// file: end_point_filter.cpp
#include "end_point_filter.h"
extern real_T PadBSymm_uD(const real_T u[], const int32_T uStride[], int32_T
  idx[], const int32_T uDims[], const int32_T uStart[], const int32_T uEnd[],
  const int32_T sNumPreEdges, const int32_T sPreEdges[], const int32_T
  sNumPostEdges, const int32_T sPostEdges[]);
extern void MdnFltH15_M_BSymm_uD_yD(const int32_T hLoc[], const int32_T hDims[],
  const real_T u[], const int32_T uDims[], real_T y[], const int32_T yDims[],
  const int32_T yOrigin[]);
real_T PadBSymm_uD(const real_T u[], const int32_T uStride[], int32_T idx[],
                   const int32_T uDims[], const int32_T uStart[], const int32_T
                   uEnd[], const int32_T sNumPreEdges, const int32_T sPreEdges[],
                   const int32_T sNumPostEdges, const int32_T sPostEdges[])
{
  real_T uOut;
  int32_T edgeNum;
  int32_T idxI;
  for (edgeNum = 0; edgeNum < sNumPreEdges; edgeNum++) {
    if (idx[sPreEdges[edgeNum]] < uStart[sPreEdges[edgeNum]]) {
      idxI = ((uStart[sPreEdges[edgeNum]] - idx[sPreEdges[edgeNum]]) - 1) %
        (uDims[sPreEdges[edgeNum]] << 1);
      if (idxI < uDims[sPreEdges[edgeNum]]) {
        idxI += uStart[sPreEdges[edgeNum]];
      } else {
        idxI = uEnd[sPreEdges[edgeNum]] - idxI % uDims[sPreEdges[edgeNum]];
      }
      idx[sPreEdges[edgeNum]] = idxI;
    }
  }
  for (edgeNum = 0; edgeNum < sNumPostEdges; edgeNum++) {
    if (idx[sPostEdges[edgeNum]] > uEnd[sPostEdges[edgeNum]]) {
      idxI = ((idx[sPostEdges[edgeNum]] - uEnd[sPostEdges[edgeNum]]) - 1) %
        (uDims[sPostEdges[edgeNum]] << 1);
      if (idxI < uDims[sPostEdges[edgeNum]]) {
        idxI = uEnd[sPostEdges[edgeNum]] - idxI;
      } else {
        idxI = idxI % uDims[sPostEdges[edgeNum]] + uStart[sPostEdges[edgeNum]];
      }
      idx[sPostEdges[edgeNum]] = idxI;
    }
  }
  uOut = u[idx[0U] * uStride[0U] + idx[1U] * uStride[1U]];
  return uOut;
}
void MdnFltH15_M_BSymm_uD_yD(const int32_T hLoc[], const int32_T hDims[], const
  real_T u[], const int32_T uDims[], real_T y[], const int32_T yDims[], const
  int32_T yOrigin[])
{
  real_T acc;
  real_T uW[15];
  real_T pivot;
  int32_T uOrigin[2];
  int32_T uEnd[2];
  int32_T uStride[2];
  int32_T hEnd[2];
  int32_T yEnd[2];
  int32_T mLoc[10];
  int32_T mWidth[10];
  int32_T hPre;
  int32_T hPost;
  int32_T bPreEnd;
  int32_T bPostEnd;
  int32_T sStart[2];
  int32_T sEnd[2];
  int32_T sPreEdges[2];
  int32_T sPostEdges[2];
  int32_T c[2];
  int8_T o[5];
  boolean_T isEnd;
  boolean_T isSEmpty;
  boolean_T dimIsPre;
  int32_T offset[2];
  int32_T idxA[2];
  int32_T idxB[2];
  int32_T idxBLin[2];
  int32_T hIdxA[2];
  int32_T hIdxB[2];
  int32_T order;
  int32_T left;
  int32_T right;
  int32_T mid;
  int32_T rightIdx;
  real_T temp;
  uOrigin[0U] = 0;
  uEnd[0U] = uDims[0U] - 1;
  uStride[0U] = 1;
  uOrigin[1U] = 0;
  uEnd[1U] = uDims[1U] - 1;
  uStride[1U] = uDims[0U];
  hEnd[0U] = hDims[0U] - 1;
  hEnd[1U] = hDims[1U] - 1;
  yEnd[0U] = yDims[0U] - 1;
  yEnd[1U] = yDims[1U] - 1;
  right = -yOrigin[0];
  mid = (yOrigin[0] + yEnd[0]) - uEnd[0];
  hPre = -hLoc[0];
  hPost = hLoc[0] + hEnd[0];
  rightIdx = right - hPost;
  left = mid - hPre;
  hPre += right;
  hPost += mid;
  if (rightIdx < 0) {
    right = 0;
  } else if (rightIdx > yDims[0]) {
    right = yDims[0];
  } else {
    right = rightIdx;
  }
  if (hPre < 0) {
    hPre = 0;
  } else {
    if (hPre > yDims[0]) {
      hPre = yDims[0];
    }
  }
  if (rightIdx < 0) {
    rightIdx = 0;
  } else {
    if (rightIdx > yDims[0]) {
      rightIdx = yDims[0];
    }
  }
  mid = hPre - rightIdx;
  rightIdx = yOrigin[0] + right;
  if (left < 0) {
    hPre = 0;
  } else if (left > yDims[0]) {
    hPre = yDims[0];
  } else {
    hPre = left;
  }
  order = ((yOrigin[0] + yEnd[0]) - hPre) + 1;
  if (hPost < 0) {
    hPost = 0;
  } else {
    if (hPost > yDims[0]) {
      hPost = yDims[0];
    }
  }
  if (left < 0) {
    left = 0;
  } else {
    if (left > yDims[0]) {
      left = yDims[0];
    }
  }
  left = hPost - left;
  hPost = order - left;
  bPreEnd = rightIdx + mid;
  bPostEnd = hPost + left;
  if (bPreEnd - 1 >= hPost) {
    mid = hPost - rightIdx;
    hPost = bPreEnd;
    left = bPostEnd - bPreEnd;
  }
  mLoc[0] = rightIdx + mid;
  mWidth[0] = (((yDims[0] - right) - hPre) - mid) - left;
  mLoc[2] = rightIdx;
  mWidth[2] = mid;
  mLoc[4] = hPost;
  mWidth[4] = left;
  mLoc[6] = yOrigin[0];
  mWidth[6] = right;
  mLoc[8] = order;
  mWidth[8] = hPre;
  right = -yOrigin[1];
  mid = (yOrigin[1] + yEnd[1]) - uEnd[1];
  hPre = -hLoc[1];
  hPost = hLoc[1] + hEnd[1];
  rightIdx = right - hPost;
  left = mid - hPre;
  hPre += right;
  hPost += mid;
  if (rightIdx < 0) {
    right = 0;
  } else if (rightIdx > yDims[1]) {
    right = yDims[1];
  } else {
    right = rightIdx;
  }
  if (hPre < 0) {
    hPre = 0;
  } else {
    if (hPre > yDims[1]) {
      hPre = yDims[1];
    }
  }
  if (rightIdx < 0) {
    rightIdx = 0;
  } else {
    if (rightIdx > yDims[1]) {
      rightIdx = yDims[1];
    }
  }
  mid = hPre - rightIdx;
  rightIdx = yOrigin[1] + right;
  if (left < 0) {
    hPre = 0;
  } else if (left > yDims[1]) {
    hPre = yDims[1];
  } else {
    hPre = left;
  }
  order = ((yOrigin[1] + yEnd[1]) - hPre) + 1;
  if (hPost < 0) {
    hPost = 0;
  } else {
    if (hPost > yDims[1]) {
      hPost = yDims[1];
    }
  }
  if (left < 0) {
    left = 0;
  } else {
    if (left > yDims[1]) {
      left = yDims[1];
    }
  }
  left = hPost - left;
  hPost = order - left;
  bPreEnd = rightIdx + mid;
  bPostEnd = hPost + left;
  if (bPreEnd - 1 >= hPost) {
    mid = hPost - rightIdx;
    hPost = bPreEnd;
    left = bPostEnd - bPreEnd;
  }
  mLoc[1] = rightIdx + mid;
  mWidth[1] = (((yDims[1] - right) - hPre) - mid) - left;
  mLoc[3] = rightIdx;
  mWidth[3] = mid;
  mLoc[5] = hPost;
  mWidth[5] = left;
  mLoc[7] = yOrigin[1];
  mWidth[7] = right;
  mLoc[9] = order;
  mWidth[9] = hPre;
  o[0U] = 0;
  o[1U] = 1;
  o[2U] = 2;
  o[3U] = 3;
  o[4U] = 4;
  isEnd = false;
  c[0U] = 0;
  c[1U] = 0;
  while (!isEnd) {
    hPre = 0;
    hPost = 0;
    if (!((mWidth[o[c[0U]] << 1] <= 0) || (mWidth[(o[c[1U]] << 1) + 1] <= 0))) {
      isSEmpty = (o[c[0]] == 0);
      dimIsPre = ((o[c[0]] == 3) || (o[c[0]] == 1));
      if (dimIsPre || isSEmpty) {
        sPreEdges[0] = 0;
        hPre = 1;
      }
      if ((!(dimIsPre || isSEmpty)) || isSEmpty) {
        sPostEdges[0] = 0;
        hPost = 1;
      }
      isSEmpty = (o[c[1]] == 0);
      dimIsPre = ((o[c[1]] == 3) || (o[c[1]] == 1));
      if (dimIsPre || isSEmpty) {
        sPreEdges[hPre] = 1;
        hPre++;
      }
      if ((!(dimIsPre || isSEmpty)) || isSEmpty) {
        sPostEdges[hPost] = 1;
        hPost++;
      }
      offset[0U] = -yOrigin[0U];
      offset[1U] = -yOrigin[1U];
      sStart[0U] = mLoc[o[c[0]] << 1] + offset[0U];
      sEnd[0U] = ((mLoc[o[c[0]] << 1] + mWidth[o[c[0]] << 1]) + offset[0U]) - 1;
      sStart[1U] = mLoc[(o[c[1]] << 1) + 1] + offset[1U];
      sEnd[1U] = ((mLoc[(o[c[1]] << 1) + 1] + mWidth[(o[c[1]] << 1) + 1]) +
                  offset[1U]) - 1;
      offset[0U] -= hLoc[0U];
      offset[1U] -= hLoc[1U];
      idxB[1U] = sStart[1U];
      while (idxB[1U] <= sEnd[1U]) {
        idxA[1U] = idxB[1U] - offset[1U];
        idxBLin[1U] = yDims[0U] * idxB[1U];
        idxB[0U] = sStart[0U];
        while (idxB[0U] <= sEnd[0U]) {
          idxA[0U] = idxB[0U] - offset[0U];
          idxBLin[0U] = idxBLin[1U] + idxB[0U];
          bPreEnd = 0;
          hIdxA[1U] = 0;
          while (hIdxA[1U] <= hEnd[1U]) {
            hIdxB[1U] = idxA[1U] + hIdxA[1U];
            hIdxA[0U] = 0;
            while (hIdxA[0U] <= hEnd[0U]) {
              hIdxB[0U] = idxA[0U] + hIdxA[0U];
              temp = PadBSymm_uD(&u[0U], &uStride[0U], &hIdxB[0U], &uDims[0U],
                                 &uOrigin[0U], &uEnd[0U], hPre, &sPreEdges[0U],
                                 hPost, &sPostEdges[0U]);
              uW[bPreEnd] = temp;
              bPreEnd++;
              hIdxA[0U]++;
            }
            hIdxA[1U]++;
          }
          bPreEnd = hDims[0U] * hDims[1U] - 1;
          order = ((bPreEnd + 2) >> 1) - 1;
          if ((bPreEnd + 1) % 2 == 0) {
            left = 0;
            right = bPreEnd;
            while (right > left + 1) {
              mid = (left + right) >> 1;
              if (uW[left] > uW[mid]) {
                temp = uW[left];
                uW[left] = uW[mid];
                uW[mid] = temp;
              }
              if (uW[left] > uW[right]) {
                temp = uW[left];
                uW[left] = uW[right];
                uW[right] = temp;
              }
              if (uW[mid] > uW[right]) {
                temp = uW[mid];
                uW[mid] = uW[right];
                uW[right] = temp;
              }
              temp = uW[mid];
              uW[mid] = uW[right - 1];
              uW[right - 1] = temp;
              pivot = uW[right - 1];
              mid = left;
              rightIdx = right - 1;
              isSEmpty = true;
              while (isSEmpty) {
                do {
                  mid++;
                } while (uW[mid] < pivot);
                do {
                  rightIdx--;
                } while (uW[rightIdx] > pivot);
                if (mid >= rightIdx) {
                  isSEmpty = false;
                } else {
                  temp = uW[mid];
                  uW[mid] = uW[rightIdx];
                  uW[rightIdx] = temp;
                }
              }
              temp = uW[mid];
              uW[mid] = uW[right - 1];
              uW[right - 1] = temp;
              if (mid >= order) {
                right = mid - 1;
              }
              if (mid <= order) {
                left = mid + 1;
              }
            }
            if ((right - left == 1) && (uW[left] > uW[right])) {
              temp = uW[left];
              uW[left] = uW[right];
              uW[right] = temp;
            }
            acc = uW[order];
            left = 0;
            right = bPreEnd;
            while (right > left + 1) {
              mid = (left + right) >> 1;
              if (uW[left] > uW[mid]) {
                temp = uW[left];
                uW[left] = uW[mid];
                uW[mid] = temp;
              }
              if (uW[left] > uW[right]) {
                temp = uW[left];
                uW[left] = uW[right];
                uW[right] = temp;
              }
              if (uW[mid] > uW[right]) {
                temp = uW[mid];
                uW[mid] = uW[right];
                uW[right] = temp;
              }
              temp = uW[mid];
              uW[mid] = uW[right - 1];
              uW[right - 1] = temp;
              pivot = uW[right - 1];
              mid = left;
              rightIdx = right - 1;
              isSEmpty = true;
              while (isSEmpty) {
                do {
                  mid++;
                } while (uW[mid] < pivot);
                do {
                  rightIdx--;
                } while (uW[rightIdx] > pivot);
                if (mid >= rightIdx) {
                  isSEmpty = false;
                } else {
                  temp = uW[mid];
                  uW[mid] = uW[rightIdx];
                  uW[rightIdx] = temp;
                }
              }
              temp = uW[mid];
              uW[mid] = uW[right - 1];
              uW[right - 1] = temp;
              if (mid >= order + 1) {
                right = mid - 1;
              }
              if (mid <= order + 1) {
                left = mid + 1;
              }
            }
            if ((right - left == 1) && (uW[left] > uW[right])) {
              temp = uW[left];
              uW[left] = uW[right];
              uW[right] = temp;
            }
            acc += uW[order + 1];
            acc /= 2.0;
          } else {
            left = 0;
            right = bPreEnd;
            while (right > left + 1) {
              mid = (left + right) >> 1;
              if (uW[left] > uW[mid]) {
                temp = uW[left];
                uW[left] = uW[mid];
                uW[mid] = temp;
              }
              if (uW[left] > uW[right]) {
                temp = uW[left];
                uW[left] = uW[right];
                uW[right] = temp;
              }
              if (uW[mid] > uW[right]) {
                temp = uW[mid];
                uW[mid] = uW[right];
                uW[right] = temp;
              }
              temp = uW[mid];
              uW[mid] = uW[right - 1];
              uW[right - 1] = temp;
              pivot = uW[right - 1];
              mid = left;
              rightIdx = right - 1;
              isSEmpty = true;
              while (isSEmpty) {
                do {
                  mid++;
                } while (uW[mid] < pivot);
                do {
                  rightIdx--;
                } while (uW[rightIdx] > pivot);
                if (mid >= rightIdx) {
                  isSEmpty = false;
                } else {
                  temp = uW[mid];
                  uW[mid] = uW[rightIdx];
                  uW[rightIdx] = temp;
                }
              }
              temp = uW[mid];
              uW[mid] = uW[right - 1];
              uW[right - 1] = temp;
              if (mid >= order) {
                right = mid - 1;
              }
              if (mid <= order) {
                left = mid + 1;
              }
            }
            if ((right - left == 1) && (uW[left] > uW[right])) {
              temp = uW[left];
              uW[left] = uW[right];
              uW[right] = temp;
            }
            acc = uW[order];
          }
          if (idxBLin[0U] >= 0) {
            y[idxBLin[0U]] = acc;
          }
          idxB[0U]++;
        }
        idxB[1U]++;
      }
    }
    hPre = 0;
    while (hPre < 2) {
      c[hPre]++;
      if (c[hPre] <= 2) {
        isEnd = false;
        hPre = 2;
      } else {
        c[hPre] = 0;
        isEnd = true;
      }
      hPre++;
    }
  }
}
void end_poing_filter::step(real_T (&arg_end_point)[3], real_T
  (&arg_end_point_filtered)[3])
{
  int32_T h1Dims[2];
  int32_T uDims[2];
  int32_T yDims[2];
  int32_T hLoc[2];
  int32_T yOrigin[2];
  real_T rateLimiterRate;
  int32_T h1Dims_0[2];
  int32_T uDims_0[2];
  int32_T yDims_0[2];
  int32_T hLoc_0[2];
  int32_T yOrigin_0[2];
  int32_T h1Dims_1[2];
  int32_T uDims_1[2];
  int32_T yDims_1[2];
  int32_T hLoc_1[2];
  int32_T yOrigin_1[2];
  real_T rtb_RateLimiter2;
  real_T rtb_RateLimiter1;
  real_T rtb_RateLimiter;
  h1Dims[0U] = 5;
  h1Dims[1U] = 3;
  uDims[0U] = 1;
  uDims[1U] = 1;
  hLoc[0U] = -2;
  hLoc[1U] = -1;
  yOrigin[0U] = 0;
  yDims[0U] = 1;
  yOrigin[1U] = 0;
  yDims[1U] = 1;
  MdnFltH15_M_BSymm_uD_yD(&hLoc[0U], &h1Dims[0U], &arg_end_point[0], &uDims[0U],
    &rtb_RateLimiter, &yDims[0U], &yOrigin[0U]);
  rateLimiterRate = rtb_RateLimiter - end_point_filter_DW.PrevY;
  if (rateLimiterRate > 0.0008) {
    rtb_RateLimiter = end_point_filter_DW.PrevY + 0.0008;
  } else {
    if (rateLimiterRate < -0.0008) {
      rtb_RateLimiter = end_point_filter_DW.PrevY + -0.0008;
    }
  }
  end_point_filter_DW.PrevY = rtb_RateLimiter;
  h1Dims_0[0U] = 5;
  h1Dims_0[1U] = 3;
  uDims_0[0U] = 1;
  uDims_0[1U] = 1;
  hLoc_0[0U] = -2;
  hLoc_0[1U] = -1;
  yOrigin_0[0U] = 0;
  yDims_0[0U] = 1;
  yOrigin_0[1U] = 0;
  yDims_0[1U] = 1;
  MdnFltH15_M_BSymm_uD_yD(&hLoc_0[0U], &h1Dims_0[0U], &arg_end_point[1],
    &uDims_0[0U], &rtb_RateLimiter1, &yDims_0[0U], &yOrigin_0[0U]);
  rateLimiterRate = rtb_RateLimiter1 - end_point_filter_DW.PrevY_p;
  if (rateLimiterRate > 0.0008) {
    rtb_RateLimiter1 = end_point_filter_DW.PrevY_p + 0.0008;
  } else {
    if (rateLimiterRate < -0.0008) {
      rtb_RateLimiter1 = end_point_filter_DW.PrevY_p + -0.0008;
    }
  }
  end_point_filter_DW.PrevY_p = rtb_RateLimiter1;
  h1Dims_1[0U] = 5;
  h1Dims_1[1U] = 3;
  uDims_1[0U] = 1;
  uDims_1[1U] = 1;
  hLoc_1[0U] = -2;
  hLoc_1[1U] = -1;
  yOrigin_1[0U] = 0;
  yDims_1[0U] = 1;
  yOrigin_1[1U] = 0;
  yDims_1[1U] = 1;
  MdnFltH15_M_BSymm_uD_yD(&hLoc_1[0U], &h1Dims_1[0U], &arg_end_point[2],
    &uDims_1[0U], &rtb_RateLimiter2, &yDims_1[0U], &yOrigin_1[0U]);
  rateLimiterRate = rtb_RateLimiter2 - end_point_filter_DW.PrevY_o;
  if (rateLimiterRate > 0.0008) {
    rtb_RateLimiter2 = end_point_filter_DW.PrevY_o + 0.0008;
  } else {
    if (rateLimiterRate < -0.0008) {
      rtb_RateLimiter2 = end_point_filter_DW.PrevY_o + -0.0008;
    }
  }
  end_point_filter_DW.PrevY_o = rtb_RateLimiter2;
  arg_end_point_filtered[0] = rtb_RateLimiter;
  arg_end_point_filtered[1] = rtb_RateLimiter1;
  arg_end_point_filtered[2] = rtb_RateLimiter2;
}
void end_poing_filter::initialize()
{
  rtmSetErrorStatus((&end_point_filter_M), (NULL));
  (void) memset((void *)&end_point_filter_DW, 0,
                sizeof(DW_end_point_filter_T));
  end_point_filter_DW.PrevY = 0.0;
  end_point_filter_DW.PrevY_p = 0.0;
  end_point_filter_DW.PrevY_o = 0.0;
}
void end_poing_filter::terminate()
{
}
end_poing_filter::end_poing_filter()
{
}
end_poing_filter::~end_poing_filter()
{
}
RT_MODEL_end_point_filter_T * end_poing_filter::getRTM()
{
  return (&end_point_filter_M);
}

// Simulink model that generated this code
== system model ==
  end_point : Inport
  end_point_filtered : Outport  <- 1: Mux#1
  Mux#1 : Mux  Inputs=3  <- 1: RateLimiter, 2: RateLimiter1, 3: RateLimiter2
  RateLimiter : RateLimiter  RisingSlewLimit=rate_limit  FallingSlewLimit=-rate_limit  <- 1: MedianFilter#1
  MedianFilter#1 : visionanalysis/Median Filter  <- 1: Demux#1
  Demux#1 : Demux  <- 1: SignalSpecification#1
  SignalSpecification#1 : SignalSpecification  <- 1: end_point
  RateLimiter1 : RateLimiter  RisingSlewLimit=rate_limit  FallingSlewLimit=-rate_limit  <- 1: MedianFilter#2
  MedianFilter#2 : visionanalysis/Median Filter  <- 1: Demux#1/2
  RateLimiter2 : RateLimiter  RisingSlewLimit=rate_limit  FallingSlewLimit=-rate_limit  <- 1: MedianFilter#3
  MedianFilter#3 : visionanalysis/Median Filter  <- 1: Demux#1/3
